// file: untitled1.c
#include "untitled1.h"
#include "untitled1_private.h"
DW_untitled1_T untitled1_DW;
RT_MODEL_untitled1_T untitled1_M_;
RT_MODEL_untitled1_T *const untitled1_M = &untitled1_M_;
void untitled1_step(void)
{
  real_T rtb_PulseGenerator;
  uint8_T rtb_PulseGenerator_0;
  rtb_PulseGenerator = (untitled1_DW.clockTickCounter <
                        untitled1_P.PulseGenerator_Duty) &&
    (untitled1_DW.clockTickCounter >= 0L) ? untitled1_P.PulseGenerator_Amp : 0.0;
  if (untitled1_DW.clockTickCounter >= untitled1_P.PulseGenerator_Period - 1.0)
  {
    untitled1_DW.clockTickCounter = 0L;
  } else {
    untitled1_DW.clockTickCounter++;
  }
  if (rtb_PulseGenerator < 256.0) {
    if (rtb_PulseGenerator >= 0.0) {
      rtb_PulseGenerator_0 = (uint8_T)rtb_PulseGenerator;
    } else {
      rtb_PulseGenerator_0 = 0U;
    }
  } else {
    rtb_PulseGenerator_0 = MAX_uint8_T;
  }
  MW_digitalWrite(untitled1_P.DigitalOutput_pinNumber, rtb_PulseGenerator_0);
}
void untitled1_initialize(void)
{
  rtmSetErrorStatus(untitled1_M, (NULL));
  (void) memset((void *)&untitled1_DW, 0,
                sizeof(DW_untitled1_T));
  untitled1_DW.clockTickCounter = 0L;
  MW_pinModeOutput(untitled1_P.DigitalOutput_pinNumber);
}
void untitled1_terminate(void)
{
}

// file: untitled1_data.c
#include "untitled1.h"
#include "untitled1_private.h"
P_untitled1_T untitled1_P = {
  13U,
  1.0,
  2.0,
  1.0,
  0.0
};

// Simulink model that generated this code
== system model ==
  DigitalOutput : arduinolib/Digital Output  pinNumber=13  <- 1: PulseGenerator
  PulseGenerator : DiscretePulseGenerator  Period=1  PulseWidth=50
